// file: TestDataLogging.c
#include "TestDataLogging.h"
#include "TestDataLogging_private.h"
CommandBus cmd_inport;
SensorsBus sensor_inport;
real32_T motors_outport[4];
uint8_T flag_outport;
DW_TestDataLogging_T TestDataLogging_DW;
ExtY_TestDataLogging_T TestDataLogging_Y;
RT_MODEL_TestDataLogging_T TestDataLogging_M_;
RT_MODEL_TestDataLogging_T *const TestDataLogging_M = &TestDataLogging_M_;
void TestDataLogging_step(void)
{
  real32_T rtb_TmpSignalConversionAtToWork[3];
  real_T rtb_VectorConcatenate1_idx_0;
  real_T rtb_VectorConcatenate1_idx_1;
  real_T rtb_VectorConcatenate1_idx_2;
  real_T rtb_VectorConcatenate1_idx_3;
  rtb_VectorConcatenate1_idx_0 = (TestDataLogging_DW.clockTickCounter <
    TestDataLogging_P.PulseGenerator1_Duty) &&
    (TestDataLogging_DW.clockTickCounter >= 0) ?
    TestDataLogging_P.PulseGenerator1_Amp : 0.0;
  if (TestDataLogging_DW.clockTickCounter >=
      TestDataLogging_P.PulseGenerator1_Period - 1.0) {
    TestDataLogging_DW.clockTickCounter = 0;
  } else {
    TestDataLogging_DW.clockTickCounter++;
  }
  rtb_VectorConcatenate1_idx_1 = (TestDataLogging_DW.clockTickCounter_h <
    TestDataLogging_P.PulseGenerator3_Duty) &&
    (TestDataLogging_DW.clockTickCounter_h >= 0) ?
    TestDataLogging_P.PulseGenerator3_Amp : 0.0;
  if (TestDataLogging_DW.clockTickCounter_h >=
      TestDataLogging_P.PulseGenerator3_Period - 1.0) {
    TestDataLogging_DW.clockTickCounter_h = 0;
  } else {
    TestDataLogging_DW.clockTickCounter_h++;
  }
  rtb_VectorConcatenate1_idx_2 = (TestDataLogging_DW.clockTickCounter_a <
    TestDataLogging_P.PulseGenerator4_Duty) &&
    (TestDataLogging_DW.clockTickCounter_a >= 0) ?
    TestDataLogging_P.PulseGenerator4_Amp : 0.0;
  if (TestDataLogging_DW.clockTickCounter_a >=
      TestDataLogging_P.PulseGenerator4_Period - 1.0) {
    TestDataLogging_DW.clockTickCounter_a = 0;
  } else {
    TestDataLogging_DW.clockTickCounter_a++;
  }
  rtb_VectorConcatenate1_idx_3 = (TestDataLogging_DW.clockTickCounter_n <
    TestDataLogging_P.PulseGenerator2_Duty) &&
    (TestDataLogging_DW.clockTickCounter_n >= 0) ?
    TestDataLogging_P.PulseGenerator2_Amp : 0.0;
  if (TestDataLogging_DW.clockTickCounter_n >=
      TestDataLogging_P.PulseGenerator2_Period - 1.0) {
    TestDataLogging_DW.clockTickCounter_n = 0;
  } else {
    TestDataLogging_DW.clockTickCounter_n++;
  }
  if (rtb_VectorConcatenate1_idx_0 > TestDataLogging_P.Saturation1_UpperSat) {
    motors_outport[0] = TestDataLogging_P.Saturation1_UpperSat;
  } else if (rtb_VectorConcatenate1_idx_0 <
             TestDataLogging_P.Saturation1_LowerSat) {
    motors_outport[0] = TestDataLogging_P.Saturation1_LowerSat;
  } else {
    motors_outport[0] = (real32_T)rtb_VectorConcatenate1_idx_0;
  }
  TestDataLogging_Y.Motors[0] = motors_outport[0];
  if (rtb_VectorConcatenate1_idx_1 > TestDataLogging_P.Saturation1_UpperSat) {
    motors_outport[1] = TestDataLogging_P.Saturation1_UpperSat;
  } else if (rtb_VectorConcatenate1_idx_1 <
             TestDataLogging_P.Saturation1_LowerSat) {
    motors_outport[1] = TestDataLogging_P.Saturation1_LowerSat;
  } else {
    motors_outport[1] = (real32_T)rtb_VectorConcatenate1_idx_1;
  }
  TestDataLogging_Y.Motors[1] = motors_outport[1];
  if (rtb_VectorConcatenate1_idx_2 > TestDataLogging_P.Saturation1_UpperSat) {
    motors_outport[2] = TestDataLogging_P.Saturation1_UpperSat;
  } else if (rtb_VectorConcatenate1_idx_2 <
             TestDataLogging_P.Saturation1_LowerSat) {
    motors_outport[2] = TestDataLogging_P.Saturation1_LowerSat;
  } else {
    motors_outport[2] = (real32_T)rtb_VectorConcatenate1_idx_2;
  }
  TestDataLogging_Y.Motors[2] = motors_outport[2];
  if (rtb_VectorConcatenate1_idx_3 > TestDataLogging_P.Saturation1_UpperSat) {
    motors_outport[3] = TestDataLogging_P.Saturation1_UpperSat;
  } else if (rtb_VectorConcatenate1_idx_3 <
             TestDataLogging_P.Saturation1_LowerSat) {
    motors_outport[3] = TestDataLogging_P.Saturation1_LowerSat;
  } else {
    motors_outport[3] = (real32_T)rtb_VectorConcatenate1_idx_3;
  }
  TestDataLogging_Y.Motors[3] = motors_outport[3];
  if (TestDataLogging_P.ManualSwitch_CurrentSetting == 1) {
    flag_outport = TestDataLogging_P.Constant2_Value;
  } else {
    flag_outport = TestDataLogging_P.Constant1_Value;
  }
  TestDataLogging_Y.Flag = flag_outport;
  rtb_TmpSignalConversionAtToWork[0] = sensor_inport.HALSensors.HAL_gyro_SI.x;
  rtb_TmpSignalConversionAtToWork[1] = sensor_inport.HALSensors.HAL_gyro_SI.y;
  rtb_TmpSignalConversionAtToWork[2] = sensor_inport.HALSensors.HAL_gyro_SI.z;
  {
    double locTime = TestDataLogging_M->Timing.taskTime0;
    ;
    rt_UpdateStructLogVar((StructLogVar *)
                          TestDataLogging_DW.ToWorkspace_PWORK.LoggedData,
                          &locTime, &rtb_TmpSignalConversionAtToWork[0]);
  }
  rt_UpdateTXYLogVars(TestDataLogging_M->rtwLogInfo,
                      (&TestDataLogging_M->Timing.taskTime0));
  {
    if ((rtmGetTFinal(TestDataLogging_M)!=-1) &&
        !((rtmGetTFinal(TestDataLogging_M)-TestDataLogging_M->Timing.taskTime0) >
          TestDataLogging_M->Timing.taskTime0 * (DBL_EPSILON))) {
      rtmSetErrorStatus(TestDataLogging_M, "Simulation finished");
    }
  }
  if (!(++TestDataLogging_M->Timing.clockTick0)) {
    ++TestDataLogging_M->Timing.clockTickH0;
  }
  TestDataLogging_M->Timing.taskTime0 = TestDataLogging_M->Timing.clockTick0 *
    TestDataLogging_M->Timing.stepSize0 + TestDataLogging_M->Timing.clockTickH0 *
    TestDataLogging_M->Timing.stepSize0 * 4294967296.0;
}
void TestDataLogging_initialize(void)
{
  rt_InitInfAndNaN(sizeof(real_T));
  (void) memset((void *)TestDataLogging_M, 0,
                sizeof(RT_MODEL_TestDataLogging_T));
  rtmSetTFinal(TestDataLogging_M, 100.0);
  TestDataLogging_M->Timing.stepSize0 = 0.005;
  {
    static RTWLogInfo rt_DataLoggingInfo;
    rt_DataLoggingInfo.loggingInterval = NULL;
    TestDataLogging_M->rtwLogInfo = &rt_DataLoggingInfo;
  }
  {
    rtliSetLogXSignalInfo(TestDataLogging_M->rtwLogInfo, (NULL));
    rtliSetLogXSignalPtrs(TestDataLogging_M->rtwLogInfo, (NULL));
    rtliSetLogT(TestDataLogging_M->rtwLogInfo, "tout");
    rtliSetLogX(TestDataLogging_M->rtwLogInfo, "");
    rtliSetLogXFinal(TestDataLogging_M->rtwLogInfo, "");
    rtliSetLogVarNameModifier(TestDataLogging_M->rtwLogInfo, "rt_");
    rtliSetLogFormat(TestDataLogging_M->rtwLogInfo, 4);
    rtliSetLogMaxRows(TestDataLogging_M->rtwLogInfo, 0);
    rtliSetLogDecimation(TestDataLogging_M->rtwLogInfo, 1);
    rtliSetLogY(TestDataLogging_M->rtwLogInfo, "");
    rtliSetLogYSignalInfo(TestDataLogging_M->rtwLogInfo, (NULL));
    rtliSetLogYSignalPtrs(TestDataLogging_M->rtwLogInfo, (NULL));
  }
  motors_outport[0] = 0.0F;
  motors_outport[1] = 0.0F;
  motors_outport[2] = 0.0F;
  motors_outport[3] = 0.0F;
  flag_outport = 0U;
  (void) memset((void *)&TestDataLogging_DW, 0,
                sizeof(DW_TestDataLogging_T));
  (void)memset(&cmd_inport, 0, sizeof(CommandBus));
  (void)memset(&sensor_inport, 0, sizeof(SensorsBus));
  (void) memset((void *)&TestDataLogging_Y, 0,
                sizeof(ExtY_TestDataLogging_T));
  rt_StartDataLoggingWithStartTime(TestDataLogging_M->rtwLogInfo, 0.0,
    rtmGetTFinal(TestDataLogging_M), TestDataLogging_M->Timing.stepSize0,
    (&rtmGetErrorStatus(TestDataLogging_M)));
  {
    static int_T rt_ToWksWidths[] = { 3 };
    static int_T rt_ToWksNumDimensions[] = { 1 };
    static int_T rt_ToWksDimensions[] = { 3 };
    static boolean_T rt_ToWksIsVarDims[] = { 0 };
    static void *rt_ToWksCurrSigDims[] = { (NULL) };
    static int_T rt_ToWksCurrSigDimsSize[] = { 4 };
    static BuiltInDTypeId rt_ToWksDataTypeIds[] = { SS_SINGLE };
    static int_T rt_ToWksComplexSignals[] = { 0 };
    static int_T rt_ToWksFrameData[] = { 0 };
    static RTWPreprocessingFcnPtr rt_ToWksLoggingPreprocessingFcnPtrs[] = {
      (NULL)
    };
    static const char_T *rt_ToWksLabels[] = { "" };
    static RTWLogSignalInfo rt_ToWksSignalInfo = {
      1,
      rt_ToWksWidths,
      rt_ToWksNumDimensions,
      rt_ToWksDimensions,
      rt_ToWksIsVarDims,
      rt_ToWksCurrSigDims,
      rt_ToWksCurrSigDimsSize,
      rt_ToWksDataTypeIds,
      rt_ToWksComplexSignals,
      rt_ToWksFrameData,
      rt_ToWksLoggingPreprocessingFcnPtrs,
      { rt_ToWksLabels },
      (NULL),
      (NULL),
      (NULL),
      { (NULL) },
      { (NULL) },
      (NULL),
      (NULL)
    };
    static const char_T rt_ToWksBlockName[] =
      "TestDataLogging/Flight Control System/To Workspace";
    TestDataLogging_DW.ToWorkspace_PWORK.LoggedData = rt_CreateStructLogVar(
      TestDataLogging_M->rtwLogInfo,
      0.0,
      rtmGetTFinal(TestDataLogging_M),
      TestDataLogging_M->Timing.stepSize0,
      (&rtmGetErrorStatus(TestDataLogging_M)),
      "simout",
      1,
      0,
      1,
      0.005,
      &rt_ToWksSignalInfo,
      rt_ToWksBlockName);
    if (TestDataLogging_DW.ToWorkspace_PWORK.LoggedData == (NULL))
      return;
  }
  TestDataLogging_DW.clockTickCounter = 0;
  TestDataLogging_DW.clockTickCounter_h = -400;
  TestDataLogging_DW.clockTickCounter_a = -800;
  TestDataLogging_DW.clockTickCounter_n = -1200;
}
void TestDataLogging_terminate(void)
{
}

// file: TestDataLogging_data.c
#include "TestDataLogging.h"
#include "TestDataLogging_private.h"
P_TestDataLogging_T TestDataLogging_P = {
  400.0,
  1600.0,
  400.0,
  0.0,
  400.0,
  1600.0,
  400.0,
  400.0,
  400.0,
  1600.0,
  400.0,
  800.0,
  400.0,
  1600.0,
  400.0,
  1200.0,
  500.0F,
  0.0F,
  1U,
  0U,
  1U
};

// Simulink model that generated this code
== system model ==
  Inport#1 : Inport
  Inport#2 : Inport
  Motors : Outport  <- 1: Saturation1
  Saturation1 : Saturate  UpperLimit=500  LowerLimit=0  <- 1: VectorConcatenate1
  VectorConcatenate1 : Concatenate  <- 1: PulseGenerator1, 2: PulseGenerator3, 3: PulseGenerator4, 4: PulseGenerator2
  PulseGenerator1 : DiscretePulseGenerator  Amplitude=400  Period=1600  PulseWidth=400
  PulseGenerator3 : DiscretePulseGenerator  Amplitude=400  Period=1600  PulseWidth=400  PhaseDelay=400
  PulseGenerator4 : DiscretePulseGenerator  Amplitude=400  Period=1600  PulseWidth=400  PhaseDelay=800
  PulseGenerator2 : DiscretePulseGenerator  Amplitude=400  Period=1600  PulseWidth=400  PhaseDelay=1200
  Flag : Outport  <- 1: ManualSwitch
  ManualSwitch : ManualSwitch  <- 1: Constant2, 2: Constant1
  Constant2 : Constant  Value=0
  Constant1 : Constant
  BusSelector#1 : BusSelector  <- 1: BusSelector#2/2
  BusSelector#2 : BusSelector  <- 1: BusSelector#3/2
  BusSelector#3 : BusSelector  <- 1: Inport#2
